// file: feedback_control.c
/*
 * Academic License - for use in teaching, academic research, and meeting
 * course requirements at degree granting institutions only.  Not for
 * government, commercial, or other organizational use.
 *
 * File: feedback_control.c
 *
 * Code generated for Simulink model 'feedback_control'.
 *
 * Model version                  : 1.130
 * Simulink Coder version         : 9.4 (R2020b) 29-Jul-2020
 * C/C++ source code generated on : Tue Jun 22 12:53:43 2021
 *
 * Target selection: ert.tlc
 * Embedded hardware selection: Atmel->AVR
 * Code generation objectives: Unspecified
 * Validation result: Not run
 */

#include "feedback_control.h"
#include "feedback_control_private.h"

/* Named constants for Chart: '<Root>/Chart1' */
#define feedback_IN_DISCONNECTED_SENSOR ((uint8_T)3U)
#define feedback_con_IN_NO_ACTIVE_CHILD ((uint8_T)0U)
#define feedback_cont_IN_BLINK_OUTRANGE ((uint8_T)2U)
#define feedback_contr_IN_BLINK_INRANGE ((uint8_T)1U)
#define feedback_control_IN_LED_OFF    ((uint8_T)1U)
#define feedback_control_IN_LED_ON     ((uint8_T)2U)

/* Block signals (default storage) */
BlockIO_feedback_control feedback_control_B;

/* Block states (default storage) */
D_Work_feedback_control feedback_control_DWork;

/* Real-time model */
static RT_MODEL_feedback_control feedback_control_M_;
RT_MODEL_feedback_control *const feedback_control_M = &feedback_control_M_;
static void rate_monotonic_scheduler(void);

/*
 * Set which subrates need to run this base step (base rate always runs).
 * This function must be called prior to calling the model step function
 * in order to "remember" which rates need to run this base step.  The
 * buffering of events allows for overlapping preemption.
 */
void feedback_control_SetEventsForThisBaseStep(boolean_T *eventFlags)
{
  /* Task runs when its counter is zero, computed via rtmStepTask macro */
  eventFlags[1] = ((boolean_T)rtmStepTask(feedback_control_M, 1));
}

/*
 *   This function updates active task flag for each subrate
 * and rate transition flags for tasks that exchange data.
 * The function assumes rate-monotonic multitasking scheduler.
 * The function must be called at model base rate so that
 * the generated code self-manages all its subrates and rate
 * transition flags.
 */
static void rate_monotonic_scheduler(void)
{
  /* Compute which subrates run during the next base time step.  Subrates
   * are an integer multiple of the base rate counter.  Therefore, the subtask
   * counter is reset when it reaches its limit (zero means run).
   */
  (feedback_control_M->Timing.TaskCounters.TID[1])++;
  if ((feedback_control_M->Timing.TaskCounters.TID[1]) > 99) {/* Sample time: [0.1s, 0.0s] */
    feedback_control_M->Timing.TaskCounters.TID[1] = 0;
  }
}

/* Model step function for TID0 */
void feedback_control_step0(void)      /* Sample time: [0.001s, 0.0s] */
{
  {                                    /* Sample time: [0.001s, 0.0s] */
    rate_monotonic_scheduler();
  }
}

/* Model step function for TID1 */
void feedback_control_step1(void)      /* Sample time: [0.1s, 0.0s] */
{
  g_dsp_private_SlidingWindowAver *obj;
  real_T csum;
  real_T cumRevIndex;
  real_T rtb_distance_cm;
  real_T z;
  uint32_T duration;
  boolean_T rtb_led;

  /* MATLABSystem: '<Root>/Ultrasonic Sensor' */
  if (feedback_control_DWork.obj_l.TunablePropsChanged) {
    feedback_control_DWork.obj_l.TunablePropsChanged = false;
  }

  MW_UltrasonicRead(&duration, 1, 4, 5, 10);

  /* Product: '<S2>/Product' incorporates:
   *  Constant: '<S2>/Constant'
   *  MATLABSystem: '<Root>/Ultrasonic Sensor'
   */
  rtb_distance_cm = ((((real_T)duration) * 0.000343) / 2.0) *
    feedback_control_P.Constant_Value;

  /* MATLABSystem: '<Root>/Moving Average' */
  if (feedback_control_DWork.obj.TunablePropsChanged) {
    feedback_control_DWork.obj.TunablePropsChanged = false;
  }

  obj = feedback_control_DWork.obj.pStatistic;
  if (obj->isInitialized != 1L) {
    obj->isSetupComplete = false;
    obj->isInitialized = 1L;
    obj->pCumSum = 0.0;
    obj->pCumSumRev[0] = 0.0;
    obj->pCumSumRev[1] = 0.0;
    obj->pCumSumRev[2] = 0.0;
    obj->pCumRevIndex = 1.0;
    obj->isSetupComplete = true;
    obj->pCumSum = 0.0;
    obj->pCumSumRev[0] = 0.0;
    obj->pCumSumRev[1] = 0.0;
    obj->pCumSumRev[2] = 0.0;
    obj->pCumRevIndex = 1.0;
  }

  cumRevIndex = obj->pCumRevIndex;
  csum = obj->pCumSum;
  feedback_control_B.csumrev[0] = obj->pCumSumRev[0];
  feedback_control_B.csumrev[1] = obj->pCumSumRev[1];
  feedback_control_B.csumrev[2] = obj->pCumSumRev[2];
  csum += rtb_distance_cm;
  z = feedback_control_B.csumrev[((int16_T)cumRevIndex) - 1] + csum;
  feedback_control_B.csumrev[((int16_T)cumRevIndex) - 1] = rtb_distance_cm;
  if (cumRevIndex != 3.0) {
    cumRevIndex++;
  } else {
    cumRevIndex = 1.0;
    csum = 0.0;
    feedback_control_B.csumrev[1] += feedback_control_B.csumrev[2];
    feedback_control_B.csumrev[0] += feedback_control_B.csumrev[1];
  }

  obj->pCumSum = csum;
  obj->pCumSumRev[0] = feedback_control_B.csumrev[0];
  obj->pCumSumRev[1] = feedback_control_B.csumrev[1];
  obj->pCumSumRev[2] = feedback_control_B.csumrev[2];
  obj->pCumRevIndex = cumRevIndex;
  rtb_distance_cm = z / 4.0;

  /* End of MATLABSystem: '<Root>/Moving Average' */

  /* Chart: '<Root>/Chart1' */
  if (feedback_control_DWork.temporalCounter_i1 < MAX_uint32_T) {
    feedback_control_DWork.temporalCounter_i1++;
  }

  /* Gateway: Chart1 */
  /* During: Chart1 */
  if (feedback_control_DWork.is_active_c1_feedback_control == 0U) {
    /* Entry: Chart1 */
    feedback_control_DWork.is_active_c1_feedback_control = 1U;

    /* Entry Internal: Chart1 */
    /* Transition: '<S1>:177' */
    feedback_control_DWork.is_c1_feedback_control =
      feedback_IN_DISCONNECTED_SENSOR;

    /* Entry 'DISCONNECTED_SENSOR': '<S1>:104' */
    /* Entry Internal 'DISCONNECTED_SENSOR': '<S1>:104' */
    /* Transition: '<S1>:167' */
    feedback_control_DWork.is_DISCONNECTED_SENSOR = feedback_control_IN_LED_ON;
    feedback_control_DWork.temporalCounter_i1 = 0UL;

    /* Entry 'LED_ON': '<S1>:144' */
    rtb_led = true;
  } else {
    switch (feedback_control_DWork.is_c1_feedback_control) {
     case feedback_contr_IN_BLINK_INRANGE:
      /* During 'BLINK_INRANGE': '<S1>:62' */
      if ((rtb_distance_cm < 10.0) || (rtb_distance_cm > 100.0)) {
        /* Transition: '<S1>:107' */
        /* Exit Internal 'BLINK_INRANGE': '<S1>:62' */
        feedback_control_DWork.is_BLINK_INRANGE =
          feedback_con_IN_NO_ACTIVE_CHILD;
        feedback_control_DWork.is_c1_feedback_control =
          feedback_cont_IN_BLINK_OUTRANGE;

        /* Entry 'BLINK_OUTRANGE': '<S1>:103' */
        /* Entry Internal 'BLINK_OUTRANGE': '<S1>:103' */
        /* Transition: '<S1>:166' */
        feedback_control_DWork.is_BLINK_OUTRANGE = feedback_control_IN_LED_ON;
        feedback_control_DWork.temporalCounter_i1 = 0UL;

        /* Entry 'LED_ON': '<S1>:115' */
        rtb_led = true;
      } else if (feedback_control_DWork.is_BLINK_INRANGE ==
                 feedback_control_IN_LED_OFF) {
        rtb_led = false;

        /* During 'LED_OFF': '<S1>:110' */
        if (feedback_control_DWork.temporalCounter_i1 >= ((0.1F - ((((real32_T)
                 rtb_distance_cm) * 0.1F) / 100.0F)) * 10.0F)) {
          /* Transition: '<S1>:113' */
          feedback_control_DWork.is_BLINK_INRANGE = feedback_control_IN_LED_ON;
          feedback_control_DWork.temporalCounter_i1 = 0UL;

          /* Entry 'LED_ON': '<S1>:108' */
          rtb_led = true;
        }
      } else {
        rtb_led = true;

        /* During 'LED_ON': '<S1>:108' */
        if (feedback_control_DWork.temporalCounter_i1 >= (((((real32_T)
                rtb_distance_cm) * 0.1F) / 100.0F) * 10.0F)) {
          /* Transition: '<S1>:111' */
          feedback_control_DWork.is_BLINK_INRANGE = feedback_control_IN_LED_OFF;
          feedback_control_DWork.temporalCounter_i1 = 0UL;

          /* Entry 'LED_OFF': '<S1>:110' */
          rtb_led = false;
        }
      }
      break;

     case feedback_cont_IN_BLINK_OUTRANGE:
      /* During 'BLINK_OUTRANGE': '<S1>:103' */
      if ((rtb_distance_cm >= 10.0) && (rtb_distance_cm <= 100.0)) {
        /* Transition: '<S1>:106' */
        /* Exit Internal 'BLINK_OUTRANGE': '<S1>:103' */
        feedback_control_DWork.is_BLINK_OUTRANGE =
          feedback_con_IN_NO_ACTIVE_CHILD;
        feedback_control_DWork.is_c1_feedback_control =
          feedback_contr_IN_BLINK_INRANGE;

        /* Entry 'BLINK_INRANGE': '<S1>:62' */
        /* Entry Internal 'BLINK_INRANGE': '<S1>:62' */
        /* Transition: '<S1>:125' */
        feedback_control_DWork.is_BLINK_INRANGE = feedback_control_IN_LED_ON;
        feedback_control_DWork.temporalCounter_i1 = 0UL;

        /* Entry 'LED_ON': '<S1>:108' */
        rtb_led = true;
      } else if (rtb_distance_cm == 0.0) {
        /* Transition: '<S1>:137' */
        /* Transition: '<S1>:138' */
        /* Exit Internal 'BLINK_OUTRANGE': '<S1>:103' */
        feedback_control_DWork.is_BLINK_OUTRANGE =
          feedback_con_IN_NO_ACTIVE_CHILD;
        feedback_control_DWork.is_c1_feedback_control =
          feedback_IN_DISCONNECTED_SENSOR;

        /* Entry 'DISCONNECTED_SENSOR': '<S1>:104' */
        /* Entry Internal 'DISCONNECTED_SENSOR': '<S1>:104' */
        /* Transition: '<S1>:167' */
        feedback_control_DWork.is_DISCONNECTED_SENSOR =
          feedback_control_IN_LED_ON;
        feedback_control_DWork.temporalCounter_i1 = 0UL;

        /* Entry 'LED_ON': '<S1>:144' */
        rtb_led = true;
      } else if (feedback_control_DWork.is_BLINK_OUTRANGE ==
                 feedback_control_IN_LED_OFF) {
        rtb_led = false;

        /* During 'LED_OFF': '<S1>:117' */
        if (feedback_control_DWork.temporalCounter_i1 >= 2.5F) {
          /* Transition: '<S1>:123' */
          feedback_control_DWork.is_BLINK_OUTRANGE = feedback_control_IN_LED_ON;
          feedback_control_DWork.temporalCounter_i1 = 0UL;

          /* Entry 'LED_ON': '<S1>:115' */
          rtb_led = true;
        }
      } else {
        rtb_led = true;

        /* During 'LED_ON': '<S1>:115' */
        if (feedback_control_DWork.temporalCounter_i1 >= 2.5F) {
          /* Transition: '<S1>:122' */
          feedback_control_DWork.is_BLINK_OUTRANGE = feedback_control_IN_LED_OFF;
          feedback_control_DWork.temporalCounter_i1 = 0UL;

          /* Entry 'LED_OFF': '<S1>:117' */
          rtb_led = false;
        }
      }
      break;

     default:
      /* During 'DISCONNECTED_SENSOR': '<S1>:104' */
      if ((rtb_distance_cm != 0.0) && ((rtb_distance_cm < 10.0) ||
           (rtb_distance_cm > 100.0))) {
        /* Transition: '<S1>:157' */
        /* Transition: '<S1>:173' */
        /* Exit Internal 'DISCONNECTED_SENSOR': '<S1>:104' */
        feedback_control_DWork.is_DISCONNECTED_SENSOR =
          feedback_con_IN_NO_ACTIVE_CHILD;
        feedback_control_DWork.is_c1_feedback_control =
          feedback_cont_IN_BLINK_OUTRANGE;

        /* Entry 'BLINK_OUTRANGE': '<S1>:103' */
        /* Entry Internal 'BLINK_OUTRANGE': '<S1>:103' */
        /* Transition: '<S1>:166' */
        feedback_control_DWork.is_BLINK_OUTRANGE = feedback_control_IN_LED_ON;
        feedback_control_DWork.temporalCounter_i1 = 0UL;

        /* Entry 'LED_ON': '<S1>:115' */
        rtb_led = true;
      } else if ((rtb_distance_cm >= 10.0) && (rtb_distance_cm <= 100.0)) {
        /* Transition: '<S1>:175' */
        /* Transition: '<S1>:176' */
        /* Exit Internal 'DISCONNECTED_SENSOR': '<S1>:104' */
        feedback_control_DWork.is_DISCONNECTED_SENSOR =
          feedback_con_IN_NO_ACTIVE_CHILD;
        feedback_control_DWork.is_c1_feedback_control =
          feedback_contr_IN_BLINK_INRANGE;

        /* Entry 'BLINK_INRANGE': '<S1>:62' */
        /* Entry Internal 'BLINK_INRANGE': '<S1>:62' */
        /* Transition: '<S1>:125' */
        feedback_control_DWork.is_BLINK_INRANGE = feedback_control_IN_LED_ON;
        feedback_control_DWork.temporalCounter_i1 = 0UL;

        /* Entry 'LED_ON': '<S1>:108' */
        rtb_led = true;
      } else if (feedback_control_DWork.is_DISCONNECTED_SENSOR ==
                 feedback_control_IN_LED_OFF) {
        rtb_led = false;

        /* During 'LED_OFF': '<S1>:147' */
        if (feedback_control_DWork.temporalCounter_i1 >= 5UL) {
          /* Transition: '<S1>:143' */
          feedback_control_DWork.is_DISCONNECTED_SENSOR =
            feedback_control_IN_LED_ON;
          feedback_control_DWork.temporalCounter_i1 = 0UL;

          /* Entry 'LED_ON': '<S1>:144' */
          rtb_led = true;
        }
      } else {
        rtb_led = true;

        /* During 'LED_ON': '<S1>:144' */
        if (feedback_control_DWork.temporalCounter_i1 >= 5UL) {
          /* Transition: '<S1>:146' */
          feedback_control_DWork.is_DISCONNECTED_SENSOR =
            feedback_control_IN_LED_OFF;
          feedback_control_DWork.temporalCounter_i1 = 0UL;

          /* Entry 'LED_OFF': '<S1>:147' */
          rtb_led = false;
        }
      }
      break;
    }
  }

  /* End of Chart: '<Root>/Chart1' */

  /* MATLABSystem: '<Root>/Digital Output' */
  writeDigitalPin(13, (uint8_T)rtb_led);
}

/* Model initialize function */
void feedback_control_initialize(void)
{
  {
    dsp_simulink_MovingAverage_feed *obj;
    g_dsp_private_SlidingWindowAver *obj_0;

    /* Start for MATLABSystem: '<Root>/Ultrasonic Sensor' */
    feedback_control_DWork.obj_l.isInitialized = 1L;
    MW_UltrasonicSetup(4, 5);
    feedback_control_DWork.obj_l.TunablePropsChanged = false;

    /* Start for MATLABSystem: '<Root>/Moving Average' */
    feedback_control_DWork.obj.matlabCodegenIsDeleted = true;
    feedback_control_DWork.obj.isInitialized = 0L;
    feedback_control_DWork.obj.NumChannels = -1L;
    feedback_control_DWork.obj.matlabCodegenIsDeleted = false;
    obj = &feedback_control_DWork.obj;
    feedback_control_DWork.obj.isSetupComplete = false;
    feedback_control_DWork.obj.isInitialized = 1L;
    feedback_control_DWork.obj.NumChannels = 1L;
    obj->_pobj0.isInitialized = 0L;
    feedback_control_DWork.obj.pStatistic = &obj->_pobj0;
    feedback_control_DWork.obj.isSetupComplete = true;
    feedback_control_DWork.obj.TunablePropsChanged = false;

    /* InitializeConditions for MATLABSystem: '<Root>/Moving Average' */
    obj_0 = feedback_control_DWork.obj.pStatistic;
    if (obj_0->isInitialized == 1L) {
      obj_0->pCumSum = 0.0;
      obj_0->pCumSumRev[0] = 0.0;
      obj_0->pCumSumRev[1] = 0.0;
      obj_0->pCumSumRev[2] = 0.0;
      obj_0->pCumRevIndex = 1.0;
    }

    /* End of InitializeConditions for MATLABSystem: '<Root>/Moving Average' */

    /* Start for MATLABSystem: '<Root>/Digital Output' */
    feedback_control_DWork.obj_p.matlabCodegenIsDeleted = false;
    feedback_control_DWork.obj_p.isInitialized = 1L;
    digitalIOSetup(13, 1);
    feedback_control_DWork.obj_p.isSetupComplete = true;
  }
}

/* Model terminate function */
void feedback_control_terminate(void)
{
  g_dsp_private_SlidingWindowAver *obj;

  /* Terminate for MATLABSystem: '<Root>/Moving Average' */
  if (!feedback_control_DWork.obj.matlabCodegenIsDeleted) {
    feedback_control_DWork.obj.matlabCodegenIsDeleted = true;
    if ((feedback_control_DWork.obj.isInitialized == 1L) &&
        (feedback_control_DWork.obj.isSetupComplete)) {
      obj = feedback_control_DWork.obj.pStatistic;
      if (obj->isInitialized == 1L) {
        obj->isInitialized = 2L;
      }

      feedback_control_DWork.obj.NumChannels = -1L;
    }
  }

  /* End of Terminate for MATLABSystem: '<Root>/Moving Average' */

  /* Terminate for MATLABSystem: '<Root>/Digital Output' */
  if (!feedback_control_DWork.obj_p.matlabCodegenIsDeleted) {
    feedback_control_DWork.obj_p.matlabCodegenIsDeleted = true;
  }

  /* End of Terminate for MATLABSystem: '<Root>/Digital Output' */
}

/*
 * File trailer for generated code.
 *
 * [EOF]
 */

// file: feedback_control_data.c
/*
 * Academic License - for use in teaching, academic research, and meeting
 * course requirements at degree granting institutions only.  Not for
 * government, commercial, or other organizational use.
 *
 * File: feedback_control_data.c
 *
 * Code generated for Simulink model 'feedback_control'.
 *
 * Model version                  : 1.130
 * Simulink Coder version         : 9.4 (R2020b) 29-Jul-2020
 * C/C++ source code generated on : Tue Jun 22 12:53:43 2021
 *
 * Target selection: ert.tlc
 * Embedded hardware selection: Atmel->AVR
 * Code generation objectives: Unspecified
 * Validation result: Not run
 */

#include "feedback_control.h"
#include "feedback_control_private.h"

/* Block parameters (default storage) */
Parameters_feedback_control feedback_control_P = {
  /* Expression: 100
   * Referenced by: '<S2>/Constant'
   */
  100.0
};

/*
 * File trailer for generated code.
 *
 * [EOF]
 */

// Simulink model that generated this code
simulink model "feedback_control"  (R2020b)
settings: Solver=FixedStepDiscrete  StartTime=0.0  StopTime=inf  FixedStep=step_size  RelTol=1e-3  EnableMultiTasking=on
libraries: arduinolib x1, dspstat3 x1, arduinosensorlib x1

== system feedback_control ==
  Chart1 : Stateflow chart  TreatAsAtomicUnit=on
  Digital Output : arduinolib/Digital Output  pinNumber=13  Direction=output  blockPlatform=arduino
  Moving Average : dspstat3/Moving Average  Method=Sliding window  ForgettingFactorPort=off  SpecifyWindowLength=on  WindowLength=4  ForgettingFactor=0.9  SimulateUsing=Code generation
  Ultrasonic Sensor : arduinosensorlib/Ultrasonic Sensor  NumSignalPins=2  TrigPin=4  EchoPin=5  SignalPin=3  SampleTime_=0.1  blockPlatform=ARDUINO
  Unit conversion : Subsystem
  wires:
  Chart1/1(led) -> Digital Output/1  "led"
  Ultrasonic Sensor/1 -> Unit conversion/1(Distance_m)  "Distance_m"
  Unit conversion/1(distance_cm) -> Moving Average/1
  Moving Average/1 -> Chart1/1(level)

== system feedback_control/Unit conversion ==
  Distance_m : Inport
  Constant : Constant  Value=100
  Product : Product
  distance_cm : Outport
  wires:
  Product/1 -> distance_cm/1  "distance_cm"
  Distance_m/1 -> Product/1
  Constant/1 -> Product/2

== stateflow chart feedback_control/Chart1 ==
  state BLINK_OUTRANGE
    frequency = 0.5;
    state LED_OFF
      entry:
      led = false;
    state LED_ON
      entry:
      led = true;
    (default) -> BLINK_OUTRANGE.LED_ON
    BLINK_OUTRANGE.LED_ON -> BLINK_OUTRANGE.LED_OFF : after(frequency/2, sec)
    BLINK_OUTRANGE.LED_OFF -> BLINK_OUTRANGE.LED_ON : after(frequency/2, sec)
  state BLINK_INRANGE
    frequency = 0.1;
    state LED_OFF
      entry:
      led = false;
    state LED_ON
      entry:
      led = true;
    (default) -> BLINK_INRANGE.LED_ON
    BLINK_INRANGE.LED_OFF -> BLINK_INRANGE.LED_ON : after(frequency - ((level*frequency)/100), sec)
    BLINK_INRANGE.LED_ON -> BLINK_INRANGE.LED_OFF : after((level*frequency)/100, sec)
  state DISCONNECTED_SENSOR
    frequency = 1;
    state LED_OFF
      entry:
      led = false;
    state LED_ON
      entry:
      led = true;
    (default) -> DISCONNECTED_SENSOR.LED_ON
    DISCONNECTED_SENSOR.LED_ON -> DISCONNECTED_SENSOR.LED_OFF : after(frequency/2, sec)
    DISCONNECTED_SENSOR.LED_OFF -> DISCONNECTED_SENSOR.LED_ON : after(frequency/2, sec)
  BLINK_OUTRANGE -> BLINK_INRANGE [order 1] : [level >=10 && level <=100]
  BLINK_INRANGE -> BLINK_OUTRANGE : [level < 10 || level >100]
  (default) -> DISCONNECTED_SENSOR
  (junction 156) -> BLINK_OUTRANGE
  BLINK_OUTRANGE -> (junction 136) [order 2] : [level == 0]
  (junction 174) -> BLINK_INRANGE
  (junction 136) -> DISCONNECTED_SENSOR
  DISCONNECTED_SENSOR -> (junction 174) [order 2] : [level >=10 && level <=100]
  DISCONNECTED_SENSOR -> (junction 156) [order 1] : [level ~= 0 && ( level < 10 || level > 100 )]
  data: led output boolean; frequency local single; level input double
